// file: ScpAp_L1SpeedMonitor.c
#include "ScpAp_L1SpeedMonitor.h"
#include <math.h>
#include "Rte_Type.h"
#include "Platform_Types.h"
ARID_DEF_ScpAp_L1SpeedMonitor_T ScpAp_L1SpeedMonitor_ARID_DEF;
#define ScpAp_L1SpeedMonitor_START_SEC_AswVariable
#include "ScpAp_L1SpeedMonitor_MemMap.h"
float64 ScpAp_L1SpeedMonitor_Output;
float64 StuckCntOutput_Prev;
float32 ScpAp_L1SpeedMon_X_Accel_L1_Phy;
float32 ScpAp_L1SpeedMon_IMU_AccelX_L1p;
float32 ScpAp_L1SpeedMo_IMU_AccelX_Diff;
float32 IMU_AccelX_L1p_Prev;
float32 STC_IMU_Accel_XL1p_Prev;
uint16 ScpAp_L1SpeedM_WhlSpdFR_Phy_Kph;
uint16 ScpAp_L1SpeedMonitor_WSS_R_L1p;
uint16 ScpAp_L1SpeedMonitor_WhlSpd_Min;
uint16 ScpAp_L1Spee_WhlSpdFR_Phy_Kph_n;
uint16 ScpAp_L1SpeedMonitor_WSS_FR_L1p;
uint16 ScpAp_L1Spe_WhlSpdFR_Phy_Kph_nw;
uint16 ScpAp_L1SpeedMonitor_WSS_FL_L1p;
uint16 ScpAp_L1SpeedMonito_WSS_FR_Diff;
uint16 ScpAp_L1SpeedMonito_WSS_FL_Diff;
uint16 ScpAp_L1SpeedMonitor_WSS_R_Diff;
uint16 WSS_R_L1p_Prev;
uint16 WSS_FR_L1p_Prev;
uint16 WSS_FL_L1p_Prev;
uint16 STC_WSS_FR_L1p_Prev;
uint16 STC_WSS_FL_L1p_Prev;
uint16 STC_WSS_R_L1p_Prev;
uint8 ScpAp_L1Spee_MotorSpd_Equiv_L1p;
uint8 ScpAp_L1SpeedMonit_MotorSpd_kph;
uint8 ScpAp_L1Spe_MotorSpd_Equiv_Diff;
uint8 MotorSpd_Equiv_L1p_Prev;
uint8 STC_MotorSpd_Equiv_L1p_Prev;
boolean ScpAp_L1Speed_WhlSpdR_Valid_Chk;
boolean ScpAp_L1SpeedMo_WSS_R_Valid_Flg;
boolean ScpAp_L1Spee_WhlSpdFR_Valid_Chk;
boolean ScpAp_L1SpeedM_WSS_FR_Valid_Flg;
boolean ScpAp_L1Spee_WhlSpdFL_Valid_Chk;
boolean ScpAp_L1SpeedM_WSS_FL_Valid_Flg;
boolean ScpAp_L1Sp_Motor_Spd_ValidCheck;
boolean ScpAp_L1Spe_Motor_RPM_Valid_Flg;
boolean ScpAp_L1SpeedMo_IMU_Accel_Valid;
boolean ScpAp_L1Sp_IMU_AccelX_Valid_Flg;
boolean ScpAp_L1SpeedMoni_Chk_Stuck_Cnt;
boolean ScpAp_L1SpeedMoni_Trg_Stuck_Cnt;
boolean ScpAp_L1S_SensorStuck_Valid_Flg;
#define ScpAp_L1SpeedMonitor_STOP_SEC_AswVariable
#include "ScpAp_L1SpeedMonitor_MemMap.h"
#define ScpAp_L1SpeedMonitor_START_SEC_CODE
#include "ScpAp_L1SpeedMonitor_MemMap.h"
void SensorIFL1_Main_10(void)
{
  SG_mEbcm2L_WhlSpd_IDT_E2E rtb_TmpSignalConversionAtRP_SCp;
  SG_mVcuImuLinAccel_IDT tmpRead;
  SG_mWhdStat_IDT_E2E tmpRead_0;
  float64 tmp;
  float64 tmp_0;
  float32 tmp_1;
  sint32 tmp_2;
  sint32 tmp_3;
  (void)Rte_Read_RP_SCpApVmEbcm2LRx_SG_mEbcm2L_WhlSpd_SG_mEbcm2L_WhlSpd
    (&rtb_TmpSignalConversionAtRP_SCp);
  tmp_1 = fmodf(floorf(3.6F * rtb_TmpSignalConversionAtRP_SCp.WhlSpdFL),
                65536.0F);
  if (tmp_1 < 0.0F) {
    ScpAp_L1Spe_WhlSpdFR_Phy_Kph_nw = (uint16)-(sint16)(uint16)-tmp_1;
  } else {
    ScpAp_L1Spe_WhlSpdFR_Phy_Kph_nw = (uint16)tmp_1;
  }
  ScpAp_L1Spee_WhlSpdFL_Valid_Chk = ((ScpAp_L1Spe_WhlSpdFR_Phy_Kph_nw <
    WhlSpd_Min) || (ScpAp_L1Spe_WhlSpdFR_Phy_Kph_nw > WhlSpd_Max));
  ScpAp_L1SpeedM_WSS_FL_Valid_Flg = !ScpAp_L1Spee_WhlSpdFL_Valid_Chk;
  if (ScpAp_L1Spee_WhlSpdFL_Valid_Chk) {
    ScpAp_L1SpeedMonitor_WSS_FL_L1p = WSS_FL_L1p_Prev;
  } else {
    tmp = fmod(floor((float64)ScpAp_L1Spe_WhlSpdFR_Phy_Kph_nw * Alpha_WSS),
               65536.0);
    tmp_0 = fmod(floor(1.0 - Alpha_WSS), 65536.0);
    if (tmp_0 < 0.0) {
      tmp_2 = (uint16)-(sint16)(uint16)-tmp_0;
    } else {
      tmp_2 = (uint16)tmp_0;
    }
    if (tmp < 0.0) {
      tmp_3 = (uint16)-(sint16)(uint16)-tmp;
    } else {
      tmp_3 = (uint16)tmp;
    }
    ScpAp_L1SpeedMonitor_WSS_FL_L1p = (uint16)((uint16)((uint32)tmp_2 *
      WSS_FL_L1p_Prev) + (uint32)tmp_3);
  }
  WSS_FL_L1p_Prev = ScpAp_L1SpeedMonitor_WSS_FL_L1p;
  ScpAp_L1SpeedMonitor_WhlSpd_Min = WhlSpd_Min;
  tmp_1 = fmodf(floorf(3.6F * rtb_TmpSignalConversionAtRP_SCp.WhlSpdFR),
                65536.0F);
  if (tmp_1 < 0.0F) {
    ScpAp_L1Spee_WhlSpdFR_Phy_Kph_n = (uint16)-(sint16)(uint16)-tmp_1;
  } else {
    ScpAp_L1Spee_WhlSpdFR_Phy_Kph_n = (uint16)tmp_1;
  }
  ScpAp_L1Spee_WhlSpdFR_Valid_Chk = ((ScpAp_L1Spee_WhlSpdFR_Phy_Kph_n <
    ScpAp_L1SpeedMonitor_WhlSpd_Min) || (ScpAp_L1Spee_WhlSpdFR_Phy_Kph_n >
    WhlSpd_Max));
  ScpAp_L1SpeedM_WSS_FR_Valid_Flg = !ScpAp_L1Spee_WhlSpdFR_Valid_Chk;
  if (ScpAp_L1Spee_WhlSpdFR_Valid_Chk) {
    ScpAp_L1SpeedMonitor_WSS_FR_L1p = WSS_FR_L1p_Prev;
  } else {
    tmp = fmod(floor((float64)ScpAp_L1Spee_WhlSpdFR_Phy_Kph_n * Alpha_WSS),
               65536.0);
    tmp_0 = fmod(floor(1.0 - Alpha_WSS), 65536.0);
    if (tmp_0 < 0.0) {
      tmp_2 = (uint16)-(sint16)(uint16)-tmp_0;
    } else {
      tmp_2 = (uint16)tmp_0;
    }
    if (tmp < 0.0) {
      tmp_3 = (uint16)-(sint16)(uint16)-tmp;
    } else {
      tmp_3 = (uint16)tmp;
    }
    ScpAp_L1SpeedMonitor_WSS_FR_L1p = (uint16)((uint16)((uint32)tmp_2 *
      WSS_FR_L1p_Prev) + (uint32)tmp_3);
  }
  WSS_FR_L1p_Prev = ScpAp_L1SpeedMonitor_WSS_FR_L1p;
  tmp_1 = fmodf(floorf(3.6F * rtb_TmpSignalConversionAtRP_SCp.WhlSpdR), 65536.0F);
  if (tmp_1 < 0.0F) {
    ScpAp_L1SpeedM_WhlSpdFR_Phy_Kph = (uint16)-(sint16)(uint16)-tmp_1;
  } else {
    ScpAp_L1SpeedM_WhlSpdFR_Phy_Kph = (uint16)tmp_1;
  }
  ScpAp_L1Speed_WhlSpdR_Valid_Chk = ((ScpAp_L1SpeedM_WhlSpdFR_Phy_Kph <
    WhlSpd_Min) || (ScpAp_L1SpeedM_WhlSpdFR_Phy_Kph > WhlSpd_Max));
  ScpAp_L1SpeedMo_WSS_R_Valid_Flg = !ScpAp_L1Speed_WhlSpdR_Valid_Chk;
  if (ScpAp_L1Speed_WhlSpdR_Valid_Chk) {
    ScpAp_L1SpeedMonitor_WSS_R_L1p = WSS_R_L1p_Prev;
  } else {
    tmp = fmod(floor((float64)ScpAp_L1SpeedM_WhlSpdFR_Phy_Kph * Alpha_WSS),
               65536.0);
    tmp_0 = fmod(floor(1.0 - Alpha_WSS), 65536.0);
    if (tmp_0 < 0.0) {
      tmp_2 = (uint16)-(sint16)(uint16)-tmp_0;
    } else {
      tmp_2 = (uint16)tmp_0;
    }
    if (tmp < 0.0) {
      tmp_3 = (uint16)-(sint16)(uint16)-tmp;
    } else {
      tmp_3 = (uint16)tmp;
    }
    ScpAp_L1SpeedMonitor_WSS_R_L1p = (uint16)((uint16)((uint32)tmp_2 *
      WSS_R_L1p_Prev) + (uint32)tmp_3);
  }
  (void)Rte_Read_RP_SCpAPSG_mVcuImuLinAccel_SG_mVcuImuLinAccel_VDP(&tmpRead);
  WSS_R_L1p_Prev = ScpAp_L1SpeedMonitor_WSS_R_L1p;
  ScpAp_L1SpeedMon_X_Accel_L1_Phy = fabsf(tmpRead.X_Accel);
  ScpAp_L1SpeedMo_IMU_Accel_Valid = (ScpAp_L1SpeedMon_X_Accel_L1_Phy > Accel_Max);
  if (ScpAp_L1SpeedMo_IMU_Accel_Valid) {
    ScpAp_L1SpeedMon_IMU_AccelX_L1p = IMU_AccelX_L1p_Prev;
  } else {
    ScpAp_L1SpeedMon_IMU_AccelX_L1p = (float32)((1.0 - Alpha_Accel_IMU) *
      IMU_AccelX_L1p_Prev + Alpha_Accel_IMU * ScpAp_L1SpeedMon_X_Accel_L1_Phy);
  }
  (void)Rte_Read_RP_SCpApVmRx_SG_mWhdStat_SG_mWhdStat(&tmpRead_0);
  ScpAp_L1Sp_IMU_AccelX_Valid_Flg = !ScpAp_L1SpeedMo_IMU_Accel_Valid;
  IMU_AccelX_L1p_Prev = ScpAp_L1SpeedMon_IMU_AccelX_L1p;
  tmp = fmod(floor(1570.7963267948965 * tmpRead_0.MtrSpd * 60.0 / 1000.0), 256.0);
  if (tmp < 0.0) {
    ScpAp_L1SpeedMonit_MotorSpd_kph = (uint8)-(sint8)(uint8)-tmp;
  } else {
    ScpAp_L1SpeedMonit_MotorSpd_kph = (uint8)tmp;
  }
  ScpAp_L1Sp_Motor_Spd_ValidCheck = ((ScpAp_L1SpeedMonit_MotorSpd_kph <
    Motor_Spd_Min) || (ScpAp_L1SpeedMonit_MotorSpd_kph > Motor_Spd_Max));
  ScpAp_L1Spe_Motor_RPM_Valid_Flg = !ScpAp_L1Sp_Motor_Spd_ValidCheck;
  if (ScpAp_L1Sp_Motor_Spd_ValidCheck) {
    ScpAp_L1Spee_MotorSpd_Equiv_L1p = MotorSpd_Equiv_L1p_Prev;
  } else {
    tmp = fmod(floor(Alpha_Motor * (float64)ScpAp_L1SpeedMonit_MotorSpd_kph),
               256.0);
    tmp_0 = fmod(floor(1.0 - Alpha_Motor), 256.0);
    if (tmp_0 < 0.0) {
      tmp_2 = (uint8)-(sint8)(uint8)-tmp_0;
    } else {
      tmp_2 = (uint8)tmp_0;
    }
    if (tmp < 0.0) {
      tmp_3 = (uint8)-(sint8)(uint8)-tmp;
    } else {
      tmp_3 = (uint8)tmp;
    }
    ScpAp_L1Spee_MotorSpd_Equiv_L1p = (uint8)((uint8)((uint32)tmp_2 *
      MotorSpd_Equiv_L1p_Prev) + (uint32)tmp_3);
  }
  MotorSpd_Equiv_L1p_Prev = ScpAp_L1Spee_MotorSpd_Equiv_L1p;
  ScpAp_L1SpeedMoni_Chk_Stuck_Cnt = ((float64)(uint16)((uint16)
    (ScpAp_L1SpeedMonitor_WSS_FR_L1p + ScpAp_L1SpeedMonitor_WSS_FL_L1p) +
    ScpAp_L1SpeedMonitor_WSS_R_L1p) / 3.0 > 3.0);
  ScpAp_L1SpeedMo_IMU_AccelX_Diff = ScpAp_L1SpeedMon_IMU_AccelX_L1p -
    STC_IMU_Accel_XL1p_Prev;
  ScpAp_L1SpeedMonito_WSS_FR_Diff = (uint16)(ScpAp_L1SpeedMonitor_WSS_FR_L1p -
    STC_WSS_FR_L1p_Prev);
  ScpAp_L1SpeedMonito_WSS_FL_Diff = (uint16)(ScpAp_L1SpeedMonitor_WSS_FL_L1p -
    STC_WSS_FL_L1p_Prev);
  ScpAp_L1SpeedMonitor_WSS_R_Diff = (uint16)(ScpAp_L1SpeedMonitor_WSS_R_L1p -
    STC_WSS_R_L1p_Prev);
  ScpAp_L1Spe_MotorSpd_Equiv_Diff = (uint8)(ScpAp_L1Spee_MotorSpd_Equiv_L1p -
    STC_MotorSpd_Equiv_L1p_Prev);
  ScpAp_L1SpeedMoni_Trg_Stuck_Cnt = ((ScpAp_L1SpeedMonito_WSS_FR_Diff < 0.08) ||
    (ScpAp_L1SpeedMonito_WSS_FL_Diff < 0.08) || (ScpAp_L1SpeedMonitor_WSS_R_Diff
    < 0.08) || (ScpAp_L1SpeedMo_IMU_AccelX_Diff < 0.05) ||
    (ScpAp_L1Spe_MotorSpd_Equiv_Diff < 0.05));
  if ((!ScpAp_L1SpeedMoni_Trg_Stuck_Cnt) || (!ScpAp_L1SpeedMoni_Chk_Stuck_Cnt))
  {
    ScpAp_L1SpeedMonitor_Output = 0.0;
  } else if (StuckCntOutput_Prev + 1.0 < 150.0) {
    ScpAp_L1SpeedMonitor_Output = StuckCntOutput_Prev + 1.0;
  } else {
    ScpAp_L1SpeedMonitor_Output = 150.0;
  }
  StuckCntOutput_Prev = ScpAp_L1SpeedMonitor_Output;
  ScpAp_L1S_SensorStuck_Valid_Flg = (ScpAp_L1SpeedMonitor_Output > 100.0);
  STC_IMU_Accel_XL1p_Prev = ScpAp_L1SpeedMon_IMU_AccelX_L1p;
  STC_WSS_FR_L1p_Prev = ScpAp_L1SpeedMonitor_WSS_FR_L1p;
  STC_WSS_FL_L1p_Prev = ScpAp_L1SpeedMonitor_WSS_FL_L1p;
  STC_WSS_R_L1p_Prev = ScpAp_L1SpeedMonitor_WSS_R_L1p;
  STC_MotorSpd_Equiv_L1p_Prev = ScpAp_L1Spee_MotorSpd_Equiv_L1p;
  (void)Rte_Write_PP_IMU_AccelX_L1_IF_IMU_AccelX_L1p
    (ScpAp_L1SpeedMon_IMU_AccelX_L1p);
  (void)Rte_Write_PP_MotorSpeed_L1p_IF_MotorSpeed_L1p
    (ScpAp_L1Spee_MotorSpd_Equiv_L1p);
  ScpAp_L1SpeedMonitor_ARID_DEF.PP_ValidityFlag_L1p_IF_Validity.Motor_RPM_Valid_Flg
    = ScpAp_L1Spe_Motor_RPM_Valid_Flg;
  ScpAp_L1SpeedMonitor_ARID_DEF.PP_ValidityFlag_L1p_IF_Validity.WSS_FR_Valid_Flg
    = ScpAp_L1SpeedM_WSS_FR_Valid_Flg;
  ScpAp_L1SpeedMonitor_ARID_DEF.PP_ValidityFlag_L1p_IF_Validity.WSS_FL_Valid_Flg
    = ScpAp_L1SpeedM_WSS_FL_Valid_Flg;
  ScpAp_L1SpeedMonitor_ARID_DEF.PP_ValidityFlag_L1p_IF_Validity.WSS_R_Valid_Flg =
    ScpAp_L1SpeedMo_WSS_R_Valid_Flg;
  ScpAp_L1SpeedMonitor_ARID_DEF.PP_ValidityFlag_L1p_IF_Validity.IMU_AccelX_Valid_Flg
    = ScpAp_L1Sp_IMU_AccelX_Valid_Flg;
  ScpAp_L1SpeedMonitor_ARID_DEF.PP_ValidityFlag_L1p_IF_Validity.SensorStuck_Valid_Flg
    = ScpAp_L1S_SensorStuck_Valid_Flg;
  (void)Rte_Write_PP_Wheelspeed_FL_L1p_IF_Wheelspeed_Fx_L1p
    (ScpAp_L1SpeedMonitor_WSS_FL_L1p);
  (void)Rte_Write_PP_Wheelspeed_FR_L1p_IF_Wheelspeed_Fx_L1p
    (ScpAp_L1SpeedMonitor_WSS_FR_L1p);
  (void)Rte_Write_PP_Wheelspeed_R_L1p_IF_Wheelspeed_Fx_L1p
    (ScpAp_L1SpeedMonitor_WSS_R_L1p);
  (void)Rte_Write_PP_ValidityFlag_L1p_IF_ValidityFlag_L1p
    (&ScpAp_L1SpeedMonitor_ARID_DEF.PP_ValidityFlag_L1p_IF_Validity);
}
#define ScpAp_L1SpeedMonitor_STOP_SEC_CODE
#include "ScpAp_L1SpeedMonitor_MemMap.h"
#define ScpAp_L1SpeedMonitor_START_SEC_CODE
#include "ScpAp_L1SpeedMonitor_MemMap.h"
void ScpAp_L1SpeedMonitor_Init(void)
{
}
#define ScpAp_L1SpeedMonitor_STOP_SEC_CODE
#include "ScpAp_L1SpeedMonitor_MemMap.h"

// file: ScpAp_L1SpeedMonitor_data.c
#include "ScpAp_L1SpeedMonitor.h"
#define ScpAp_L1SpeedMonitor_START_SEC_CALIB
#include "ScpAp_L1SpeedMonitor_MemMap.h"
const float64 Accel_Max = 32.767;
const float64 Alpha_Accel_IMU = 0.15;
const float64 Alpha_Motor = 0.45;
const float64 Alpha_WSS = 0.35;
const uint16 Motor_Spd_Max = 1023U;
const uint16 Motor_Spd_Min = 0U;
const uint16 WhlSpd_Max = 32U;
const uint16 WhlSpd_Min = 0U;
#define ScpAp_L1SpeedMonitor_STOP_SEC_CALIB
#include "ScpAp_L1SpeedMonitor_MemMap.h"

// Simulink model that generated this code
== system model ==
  RP_SCpAPSG_mVcuImuLinAccel_SG_mVcuImuLinAccel_VDP : Inport
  RP_SCpApVmEbcm2LRx_SG_mEbcm2L_WhlSpd_SG_mEbcm2L_WhlSpd : Inport
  RP_SCpApVmRx_SG_mWhdStat_SG_mWhdStat : Inport
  PP_IMU_AccelX_L1_IF_IMU_AccelX_L1p : Outport  <- 1: Subsystem#1
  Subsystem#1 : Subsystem  <- 1: RP_SCpAPSG_mVcuImuLinAccel_SG_mVcuImuLinAccel_VDP, 2: RP_SCpApVmEbcm2LRx_SG_mEbcm2L_WhlSpd_SG_mEbcm2L_WhlSpd, 3: RP_SCpApVmRx_SG_mWhdStat_SG_mWhdStat
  PP_MotorSpeed_L1p_IF_MotorSpeed_L1p : Outport  <- 1: Subsystem#1/2
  PP_ValidityFlag_L1p_IF_ValidityFlag_L1p : Outport  <- 1: Subsystem#1/3
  PP_Wheelspeed_FL_L1p_IF_Wheelspeed_Fx_L1p : Outport  <- 1: Subsystem#1/4
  PP_Wheelspeed_FR_L1p_IF_Wheelspeed_Fx_L1p : Outport  <- 1: Subsystem#1/5
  PP_Wheelspeed_R_L1p_IF_Wheelspeed_Fx_L1p : Outport  <- 1: Subsystem#1/6
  EventListener#1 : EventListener
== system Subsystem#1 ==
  Inport#1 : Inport
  Inport#2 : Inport
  Inport#3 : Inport
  Outport#1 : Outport  <- 1: Subsystem#2/8
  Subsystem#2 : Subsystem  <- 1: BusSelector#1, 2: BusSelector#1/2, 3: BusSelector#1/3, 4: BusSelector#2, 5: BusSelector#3
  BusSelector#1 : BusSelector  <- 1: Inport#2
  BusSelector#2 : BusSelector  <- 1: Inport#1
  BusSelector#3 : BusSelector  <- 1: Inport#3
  Outport#2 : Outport  <- 1: Subsystem#2/10
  Outport#3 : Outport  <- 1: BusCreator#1
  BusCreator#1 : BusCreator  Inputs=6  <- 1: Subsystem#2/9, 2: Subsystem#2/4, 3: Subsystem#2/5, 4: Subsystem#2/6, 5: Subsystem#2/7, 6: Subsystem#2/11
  Outport#4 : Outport  <- 1: Subsystem#2/2
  Outport#5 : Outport  <- 1: Subsystem#2
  Outport#6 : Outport  <- 1: Subsystem#2/3
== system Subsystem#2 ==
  Inport#4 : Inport
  Inport#5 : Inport
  Inport#6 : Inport
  X_Accel_L1 : Inport
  Inport#7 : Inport
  Outport#7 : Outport  <- 1: Subsystem#3
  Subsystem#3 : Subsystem  <- 1: Inport#4, 2: Inport#5, 3: Inport#6, 4: X_Accel_L1, 5: Inport#7
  Outport#8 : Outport  <- 1: Subsystem#3/2
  Outport#9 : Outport  <- 1: Subsystem#3/3
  WSS_FR_Valid_Flg : Outport  <- 1: Subsystem#3/4
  WSS_FL_Valid_Flg : Outport  <- 1: Subsystem#3/5
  WSS_R_Valid_Flg : Outport  <- 1: Subsystem#3/6
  IMU_AccelX_Valid_Flg : Outport  <- 1: Subsystem#3/7
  IMU_AccelX_L1p : Outport  <- 1: Subsystem#3/8
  Outport#10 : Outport  <- 1: Subsystem#3/9
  Outport#11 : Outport  <- 1: Subsystem#3/10
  SensorStuck_Valid_Flg : Outport  <- 1: Subsystem#4
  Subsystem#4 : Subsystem  <- 1: Subsystem#3, 2: Subsystem#3/2, 3: Subsystem#3/3, 4: Subsystem#3/8, 5: Subsystem#3/10
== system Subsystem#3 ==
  Inport#8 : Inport
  Inport#9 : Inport
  Inport#10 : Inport
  Inport#11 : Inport
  Inport#12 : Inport
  WSS_FR_L1p : Outport  <- 1: WSS/2
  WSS : Subsystem  <- 1: Inport#8, 2: Inport#9, 3: Inport#10, 4: Constant#1
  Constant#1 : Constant  Value=Alpha_WSS
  WSS_FL_L1p : Outport  <- 1: WSS/4
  WSS_R_L1p : Outport  <- 1: WSS/6
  Outport#12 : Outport  <- 1: WSS
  Outport#13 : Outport  <- 1: WSS/3
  Outport#14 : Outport  <- 1: WSS/5
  Outport#15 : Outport  <- 1: IMU
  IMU : Subsystem  <- 1: Inport#11, 2: Constant#2
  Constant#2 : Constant  Value=Alpha_Accel_IMU
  Outport#16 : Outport  <- 1: IMU/2
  Outport#17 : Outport  <- 1: Motor
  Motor : Subsystem  <- 1: Inport#12, 2: Constant#3
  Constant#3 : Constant  Value=Alpha_Motor
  MotorSpd_Equiv_L1p : Outport  <- 1: Motor/2
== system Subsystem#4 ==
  Inport#13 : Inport
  Inport#14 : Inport
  Inport#15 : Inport
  Inport#16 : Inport
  Inport#17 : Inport
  Outport#18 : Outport  <- 1: Subsystem#5
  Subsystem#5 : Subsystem  <- 1: Switch#1, 2: Inport#13, 3: Inport#14, 4: Inport#15, 5: Inport#16, 6: Inport#17
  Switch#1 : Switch  Criteria=u2 > Threshold  <- 1: Constant#4, 2: RelationalOperator#1, 3: Constant#5
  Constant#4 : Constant
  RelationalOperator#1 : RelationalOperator  Operator=>  <- 1: Product#1, 2: Constant#6
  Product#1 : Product  Inputs=*/  <- 1: Sum#1, 2: Constant#7
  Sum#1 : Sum  Inputs=+++  <- 1: Inport#13, 2: Inport#14, 3: Inport#15
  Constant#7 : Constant  Value=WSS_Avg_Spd
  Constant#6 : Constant  Value=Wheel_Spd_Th
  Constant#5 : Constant  Value=0
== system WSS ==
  Inport#18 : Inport
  Inport#19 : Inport
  Inport#20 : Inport
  Alpha_WSS : Inport
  Outport#19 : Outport  <- 1: WSS_FR
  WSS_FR : Subsystem  <- 1: Inport#18, 2: Alpha_WSS
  Outport#20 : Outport  <- 1: WSS_FR/2
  Outport#21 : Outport  <- 1: WSS_FL
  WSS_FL : Subsystem  <- 1: Inport#19, 2: Alpha_WSS
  Outport#22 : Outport  <- 1: WSS_FL/2
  Outport#23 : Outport  <- 1: WSS_R
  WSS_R : Subsystem  <- 1: Inport#20, 2: Alpha_WSS
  Outport#24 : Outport  <- 1: WSS_R/2
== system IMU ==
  Inport#21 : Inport
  Alpha_Accel_IMU : Inport
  Outport#25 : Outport  <- 1: Switch#2
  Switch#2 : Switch  Criteria=u2 > Threshold  <- 1: Constant#8, 2: RelationalOperator#2, 3: Constant#9
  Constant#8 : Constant  Value=0
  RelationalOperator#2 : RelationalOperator  Operator=>  <- 1: Abs#1, 2: Constant#10
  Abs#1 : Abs  <- 1: Inport#21
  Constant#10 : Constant  Value=Accel_Max
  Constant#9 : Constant
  Outport#26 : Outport  <- 1: Switch#3
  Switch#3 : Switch  Criteria=u2 > Threshold  <- 1: UnitDelay#1, 2: RelationalOperator#2, 3: Subsystem#6
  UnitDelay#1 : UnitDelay  <- 1: Switch#3
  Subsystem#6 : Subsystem  <- 1: Abs#1, 2: UnitDelay#1, 3: Alpha_Accel_IMU
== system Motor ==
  Inport#22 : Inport
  Alpha_Motor : Inport
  Motor_RPM_Valid_Flg : Outport  <- 1: Switch#4
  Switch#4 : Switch  Criteria=u2 > Threshold  <- 1: Constant#11, 2: Logic#1, 3: Constant#12
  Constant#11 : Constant  Value=0
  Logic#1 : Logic  Operator=OR  <- 1: RelationalOperator#3, 2: RelationalOperator#4
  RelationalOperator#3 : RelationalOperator  Operator=<  <- 1: Subsystem#7, 2: Constant#13
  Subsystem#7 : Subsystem  <- 1: Inport#22
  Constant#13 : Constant  Value=Motor_Spd_Min
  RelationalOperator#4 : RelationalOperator  Operator=>  <- 1: Subsystem#7, 2: Constant#14
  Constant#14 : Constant  Value=Motor_Spd_Max
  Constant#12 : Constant
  Outport#27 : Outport  <- 1: Switch#5
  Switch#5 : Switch  Criteria=u2 > Threshold  <- 1: UnitDelay#2, 2: Logic#1, 3: Subsystem#8
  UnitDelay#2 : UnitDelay  <- 1: Switch#5
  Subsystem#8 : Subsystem  <- 1: Subsystem#7, 2: UnitDelay#2, 3: Alpha_Motor
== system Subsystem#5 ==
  Chk_Stuck_Cnt : Inport
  Inport#23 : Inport
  Inport#24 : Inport
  Inport#25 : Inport
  Inport#26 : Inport
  Inport#27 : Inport
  Outport#28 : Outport  <- 1: Switch#6
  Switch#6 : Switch  Criteria=u2 > Threshold  <- 1: Constant#15, 2: RelationalOperator#5, 3: Constant#16
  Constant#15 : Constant
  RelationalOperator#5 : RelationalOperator  Operator=>  <- 1: Subsystem#9, 2: Constant#17
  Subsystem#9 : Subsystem  <- 1: Logic#2, 2: Chk_Stuck_Cnt
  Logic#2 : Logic  Operator=OR  Inputs=5  <- 1: RelationalOperator#6, 2: RelationalOperator#7, 3: RelationalOperator#8, 4: RelationalOperator#9, 5: RelationalOperator#10
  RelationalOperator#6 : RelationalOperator  Operator=<  <- 1: Sum#2, 2: Constant#18
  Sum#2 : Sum  Inputs=+-  <- 1: Inport#23, 2: UnitDelay#3
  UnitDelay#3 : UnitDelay  <- 1: Inport#23
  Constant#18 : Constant  Value=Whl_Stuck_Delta
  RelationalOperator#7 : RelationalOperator  Operator=<  <- 1: Sum#3, 2: Constant#19
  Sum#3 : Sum  Inputs=+-  <- 1: Inport#24, 2: UnitDelay#4
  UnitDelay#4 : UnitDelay  <- 1: Inport#24
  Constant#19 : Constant  Value=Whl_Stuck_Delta
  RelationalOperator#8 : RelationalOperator  Operator=<  <- 1: Sum#4, 2: Constant#20
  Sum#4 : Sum  Inputs=+-  <- 1: Inport#25, 2: UnitDelay#5
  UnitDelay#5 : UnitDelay  <- 1: Inport#25
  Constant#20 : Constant  Value=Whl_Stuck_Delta
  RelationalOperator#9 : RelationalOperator  Operator=<  <- 1: Sum#5, 2: Constant#21
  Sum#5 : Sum  Inputs=+-  <- 1: Inport#26, 2: UnitDelay#6
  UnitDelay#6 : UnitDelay  <- 1: Inport#26
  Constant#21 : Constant  Value=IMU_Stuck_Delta
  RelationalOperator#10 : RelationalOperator  Operator=<  <- 1: Sum#6, 2: Constant#22
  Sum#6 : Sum  Inputs=+-  <- 1: Inport#27, 2: UnitDelay#7
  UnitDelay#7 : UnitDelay  <- 1: Inport#27
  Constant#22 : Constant  Value=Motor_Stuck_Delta
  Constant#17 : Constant  Value=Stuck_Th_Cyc
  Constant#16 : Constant  Value=0
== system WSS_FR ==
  Inport#28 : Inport
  Inport#29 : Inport
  Outport#29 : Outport  <- 1: Switch#7
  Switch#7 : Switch  Criteria=u2 > Threshold  <- 1: Constant#23, 2: Logic#3, 3: Constant#24
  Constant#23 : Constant  Value=0
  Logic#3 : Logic  Operator=OR  <- 1: RelationalOperator#11, 2: RelationalOperator#12
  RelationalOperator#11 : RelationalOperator  Operator=<  <- 1: DataTypeConversion#1, 2: Constant#25
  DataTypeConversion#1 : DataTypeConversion  <- 1: Gain#1
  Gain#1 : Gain  Gain=3.6  <- 1: Inport#28
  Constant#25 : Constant  Value=WhlSpd_Min
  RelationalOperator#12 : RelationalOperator  Operator=>  <- 1: DataTypeConversion#1, 2: Constant#26
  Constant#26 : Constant  Value=WhlSpd_Max
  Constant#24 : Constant
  Outport#30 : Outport  <- 1: Switch#8
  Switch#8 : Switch  Criteria=u2 > Threshold  <- 1: UnitDelay#8, 2: Logic#3, 3: Subsystem#10
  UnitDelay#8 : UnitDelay  <- 1: Switch#8
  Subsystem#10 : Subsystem  <- 1: DataTypeConversion#1, 2: UnitDelay#8, 3: Inport#29
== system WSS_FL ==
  Inport#30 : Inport
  Inport#31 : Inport
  Outport#31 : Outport  <- 1: Switch#9
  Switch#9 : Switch  Criteria=u2 > Threshold  <- 1: Constant#27, 2: Logic#4, 3: Constant#28
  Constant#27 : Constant  Value=0
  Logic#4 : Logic  Operator=OR  <- 1: RelationalOperator#13, 2: RelationalOperator#14
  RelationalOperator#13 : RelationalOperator  Operator=<  <- 1: DataTypeConversion#2, 2: Constant#29
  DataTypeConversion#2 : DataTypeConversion  <- 1: Gain#2
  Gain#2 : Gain  Gain=3.6  <- 1: Inport#30
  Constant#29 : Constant  Value=WhlSpd_Min
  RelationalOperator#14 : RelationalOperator  Operator=>  <- 1: DataTypeConversion#2, 2: Constant#30
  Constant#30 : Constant  Value=WhlSpd_Max
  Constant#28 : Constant
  Outport#32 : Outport  <- 1: Switch#10
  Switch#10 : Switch  Criteria=u2 > Threshold  <- 1: UnitDelay#9, 2: Logic#4, 3: Subsystem#11
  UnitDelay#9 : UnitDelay  <- 1: Switch#10
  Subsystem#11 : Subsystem  <- 1: DataTypeConversion#2, 2: UnitDelay#9, 3: Inport#31
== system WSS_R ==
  Inport#32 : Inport
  Inport#33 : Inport
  Outport#33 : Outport  <- 1: Switch#11
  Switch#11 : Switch  Criteria=u2 > Threshold  <- 1: Constant#31, 2: Logic#5, 3: Constant#32
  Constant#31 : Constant  Value=0
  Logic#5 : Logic  Operator=OR  <- 1: RelationalOperator#15, 2: RelationalOperator#16
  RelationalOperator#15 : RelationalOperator  Operator=<  <- 1: DataTypeConversion#3, 2: Constant#33
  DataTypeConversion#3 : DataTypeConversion  <- 1: Gain#3
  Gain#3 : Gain  Gain=3.6  <- 1: Inport#32
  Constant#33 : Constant  Value=WhlSpd_Min
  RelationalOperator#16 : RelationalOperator  Operator=>  <- 1: DataTypeConversion#3, 2: Constant#34
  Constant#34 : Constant  Value=WhlSpd_Max
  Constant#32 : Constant
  Outport#34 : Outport  <- 1: Switch#12
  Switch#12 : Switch  Criteria=u2 > Threshold  <- 1: UnitDelay#10, 2: Logic#5, 3: Subsystem#12
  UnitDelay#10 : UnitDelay  <- 1: Switch#12
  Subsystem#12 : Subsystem  <- 1: DataTypeConversion#3, 2: UnitDelay#10, 3: Inport#33
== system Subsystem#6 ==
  X_Accel_L1_Phy : Inport
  IMU_AccelX_L1p_Prev : Inport
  Inport#34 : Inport
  Outport#35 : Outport  <- 1: Sum#7
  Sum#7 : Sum  <- 1: Product#2, 2: Product#3
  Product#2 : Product  <- 1: Inport#34, 2: X_Accel_L1_Phy
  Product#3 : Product  <- 1: Sum#8, 2: IMU_AccelX_L1p_Prev
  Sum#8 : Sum  Inputs=+-  <- 1: Constant#35, 2: Inport#34
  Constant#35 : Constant
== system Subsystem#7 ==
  Inport#35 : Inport
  MotorSpd_kph : Outport  <- 1: DataTypeConversion#4
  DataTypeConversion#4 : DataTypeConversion  <- 1: Product#4
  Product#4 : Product  Inputs=*/  <- 1: Product#5, 2: Constant#36
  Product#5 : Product  Inputs=4  <- 1: Constant#37, 2: Constant#38, 3: Inport#35, 4: Constant#39
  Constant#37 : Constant  Value=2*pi
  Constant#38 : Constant  Value=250
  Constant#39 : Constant  Value=60
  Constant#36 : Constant  Value=1000
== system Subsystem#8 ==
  Inport#36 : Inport
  MotorSpd_Equiv_L1p_Prev : Inport
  Inport#37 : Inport
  Outport#36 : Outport  <- 1: Sum#9
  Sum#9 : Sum  <- 1: Product#6, 2: Product#7
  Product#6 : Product  <- 1: Inport#37, 2: Inport#36
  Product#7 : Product  <- 1: Sum#10, 2: MotorSpd_Equiv_L1p_Prev
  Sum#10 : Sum  Inputs=+-  <- 1: Constant#40, 2: Inport#37
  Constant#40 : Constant
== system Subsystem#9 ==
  Trg_Stuck_Cnt : Inport
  Inport#38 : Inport
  Output : Outport  <- 1: Switch#13
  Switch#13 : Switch  Criteria=u2 > Threshold  <- 1: Constant#41, 2: Logic#6, 3: Switch#14
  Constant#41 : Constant  Value=0
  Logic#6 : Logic  Operator=OR  <- 1: RelationalOperator#17, 2: RelationalOperator#18
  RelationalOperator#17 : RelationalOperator  Operator===  <- 1: Trg_Stuck_Cnt, 2: Constant#42
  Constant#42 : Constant  Value=0
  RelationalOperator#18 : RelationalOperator  Operator===  <- 1: Inport#38, 2: Constant#43
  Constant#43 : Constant  Value=0
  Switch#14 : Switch  Criteria=u2 > Threshold  <- 1: Sum#11, 2: RelationalOperator#19, 3: Constant#44
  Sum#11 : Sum  <- 1: Trg_Stuck_Cnt, 2: UnitDelay#11
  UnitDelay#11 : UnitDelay  <- 1: Switch#13
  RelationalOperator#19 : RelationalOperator  Operator=<  <- 1: Sum#11, 2: Constant#45
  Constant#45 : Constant  Value=150
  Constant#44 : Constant  Value=150
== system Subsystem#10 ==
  WhlSpdFR_Phy_Kph : Inport
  WSS_FR_L1p_Prev : Inport
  Inport#39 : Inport
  Outport#37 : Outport  <- 1: Sum#12
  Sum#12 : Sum  <- 1: Product#8, 2: Product#9
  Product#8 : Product  <- 1: WhlSpdFR_Phy_Kph, 2: Inport#39
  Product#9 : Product  <- 1: Sum#13, 2: WSS_FR_L1p_Prev
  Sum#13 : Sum  Inputs=+-  <- 1: Constant#46, 2: Inport#39
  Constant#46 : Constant
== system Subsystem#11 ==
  Inport#40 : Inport
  WSS_FL_L1p_Prev : Inport
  Alpha : Inport
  Outport#38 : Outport  <- 1: Sum#14
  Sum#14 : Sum  <- 1: Product#10, 2: Product#11
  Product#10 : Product  <- 1: Inport#40, 2: Alpha
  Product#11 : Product  <- 1: Sum#15, 2: WSS_FL_L1p_Prev
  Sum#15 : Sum  Inputs=+-  <- 1: Constant#47, 2: Alpha
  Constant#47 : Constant
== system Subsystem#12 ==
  Inport#41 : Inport
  WSS_R_L1p_Prev : Inport
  Inport#42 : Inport
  Outport#39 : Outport  <- 1: Sum#16
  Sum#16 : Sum  <- 1: Product#12, 2: Product#13
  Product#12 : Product  <- 1: Inport#41, 2: Inport#42
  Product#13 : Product  <- 1: Sum#17, 2: WSS_R_L1p_Prev
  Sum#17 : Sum  Inputs=+-  <- 1: Constant#48, 2: Inport#42
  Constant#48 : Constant
